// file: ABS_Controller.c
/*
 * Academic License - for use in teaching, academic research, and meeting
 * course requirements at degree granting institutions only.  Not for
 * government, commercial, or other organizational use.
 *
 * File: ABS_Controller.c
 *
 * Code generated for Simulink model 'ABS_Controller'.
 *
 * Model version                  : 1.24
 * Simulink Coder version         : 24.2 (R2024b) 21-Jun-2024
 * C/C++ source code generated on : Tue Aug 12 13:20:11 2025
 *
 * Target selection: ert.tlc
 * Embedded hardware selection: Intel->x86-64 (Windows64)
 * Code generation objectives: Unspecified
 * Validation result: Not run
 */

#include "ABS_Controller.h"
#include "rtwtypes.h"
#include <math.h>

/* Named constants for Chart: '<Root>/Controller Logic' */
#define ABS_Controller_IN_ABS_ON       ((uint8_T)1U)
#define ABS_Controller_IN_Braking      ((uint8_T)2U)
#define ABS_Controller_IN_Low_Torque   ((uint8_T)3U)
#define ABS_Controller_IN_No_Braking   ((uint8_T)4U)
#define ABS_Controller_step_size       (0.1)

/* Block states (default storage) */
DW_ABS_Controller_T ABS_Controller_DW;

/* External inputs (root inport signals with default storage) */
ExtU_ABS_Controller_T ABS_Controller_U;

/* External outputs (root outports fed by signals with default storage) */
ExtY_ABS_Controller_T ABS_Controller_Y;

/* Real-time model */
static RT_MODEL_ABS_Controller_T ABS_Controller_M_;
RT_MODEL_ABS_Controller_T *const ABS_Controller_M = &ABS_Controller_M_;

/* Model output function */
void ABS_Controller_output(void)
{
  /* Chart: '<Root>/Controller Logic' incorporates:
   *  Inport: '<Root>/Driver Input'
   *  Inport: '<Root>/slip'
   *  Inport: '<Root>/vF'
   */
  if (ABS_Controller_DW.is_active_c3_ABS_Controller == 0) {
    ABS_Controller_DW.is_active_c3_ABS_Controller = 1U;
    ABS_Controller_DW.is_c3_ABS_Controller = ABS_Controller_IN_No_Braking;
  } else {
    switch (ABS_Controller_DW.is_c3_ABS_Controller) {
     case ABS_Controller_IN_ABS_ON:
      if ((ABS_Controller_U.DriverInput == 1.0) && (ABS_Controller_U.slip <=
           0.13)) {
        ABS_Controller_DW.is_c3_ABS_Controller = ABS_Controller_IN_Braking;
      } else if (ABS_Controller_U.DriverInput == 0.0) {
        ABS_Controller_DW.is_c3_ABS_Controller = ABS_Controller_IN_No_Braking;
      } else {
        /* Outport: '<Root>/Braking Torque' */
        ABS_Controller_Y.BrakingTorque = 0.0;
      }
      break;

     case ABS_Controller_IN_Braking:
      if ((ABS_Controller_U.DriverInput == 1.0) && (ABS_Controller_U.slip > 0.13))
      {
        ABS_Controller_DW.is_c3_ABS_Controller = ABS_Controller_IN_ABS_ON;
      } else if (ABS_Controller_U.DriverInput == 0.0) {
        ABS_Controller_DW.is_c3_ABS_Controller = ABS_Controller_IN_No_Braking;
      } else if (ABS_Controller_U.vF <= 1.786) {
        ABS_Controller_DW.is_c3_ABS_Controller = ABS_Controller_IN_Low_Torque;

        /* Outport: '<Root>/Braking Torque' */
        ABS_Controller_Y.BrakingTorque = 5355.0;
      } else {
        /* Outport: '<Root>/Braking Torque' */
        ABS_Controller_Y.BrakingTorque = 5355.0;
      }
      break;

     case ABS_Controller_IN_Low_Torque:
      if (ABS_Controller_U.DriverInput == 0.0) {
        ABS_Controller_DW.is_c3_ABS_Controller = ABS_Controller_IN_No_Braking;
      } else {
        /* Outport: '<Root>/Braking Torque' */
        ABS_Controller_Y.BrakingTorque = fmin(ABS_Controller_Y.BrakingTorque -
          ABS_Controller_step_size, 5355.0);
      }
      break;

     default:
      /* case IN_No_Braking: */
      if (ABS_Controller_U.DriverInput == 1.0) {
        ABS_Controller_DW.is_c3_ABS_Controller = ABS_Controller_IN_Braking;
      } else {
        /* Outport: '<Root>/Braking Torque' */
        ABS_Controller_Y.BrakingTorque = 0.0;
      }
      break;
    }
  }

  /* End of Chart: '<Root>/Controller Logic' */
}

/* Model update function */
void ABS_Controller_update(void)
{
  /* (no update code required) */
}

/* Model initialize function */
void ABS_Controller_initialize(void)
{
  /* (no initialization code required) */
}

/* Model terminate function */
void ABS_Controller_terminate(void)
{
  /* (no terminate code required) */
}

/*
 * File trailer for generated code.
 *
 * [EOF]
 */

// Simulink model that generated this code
simulink model "ABS_Controller"  (R2024b)
settings: Solver=FixedStepDiscrete  StartTime=0.0  StopTime=10  FixedStep=0.0001  RelTol=1e-3

== system ABS_Controller ==
  slip : Inport  OutDataTypeStr=double  PortDimensions=1
  vF : Inport  Port=2  OutDataTypeStr=double  PortDimensions=1
  Driver Input : Inport  Port=3  OutDataTypeStr=double  PortDimensions=1
  Controller Logic : Stateflow chart  TreatAsAtomicUnit=on  SystemSampleTime=0.0001
  Braking Torque : Outport  OutDataTypeStr=double  PortDimensions=1  SampleTime=[0.0001,0]
  wires:
  slip/1 -> Controller Logic/1(slip)
  Controller Logic/1(Braking_Torque) -> Braking Torque/1
  Driver Input/1 -> Controller Logic/3(Driver_Input)
  vF/1 -> Controller Logic/2(vF)

== stateflow chart ABS_Controller/Controller Logic ==
  state Low_Torque
    entry: Braking_Torque=BT_max;
    during: Braking_Torque=min(Braking_Torque - step_size , BT_max);
  state Braking
    during: Braking_Torque=BT_max;
  state No_Braking
    during: Braking_Torque=0;
  state ABS_ON
    during: Braking_Torque=0;
  Low_Torque -> No_Braking : [Driver_Input == 0]
  Braking -> Low_Torque [order 3] : [vF <= 1.786]
  (default) -> No_Braking
  No_Braking -> Braking : [Driver_Input == 1]
  Braking -> No_Braking [order 2] : [Driver_Input == 0]
  ABS_ON -> No_Braking [order 2] : [Driver_Input == 0]
  ABS_ON -> Braking [order 1] : [Driver_Input == 1 && slip <= 0.13]
  Braking -> ABS_ON [order 1] : [Driver_Input == 1 && slip > 0.13]
  data: slip input; vF input; Driver_Input input; Braking_Torque output; BT_max parameter; step_size constant double =0.1
